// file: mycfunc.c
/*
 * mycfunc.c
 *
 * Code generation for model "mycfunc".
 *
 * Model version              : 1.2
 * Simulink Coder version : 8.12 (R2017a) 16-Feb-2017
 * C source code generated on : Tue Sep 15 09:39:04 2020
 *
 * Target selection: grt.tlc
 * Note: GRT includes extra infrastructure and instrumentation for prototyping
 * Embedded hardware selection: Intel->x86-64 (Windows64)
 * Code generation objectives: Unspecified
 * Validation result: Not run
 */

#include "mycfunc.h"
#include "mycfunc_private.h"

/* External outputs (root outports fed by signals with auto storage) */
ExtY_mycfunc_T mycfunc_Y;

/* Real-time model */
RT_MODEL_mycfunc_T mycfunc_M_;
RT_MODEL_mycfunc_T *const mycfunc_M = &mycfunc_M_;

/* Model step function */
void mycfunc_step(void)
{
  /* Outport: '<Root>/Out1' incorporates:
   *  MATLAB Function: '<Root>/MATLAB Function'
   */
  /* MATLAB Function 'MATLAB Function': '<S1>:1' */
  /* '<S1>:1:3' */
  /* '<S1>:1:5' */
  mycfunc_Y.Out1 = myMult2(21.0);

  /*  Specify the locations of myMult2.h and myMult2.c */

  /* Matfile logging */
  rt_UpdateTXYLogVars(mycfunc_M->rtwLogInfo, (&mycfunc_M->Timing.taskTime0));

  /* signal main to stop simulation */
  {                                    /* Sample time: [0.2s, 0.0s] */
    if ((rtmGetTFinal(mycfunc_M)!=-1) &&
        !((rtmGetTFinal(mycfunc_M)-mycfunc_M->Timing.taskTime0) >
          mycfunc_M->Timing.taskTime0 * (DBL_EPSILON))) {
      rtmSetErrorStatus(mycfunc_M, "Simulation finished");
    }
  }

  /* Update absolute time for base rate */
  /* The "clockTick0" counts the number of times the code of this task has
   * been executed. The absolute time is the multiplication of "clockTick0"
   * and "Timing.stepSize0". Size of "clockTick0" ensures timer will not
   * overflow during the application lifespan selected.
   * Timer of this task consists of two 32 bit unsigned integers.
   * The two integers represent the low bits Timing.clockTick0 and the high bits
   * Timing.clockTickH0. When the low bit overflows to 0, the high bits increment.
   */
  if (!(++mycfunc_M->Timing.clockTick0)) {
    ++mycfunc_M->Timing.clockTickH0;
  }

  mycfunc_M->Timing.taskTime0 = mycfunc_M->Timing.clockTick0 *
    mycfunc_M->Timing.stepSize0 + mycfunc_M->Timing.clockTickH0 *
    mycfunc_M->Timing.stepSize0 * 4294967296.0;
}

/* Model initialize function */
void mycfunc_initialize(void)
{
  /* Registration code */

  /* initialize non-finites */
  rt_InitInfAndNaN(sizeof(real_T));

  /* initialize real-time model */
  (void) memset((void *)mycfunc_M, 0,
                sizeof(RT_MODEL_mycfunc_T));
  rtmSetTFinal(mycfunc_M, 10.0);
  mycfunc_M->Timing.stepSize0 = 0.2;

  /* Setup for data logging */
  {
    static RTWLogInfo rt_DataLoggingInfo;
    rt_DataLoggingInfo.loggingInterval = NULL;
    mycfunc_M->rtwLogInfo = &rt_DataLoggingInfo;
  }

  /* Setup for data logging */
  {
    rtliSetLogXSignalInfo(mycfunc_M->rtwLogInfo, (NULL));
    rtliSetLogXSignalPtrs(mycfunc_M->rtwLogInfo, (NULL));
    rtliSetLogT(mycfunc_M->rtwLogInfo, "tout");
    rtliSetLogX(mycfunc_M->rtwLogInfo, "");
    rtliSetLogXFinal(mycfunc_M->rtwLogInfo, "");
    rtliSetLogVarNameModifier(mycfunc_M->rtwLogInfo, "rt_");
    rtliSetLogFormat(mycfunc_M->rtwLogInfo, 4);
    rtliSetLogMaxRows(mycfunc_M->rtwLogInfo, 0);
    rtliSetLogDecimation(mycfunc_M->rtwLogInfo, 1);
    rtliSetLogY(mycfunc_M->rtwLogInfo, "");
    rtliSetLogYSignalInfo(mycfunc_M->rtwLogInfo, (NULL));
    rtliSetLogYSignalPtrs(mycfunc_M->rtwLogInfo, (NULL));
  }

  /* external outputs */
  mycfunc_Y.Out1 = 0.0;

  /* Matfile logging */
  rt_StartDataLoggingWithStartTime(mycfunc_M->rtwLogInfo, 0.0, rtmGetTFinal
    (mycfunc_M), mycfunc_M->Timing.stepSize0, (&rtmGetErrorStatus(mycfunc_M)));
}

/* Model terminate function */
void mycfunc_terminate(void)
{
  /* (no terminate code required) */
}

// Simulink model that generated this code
simulink model "mycfunc"  (R2017a)
settings: Solver=FixedStepAuto  StartTime=0.0  StopTime=10.0  RelTol=1e-3

== system mycfunc ==
  MATLAB Function : MATLAB Function  TreatAsAtomicUnit=on
  Out1 : Outport
  wires:
  MATLAB Function/1(y) -> Out1/1

== matlab function mycfunc/MATLAB Function ==
function y = myfunc
%#codegen
y = 21;
coder.cinclude('myMult2.h');
y = coder.ceval('myMult2', y);
% Specify the locations of myMult2.h and myMult2.c
coder.extrinsic('pwd', 'fullfile');
customDir = coder.const(fullfile(pwd, 'mycfiles'));
coder.updateBuildInfo('addIncludePaths', customDir);
coder.updateBuildInfo('addSourcePaths', customDir);
coder.updateBuildInfo('addSourceFiles', 'myMult2.c');
end
